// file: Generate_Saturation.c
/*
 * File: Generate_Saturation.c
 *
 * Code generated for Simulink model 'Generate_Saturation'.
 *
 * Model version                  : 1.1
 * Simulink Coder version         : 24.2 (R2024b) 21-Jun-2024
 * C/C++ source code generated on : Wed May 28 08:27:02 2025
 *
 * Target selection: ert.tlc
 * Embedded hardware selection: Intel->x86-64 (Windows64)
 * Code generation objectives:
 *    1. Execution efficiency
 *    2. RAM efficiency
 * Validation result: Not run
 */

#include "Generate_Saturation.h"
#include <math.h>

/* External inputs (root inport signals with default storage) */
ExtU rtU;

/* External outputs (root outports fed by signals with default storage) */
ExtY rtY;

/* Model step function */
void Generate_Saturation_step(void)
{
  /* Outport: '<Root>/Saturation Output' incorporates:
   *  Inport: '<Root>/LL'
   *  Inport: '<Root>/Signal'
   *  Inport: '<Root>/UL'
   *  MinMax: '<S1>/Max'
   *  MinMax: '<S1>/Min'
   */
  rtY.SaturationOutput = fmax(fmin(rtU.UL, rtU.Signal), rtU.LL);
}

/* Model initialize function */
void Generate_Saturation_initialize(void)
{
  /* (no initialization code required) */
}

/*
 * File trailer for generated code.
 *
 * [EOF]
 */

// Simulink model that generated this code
simulink model "Generate_Saturation"  (R2024b)
settings: Solver=FixedStepDiscrete  StartTime=0.0  StopTime=10.0  FixedStep=0.001  RelTol=1e-3

== system Generate_Saturation ==
  Signal : Inport
  UL : Inport  Port=2
  LL : Inport  Port=3
  Saturation : Subsystem
  Saturation Output : Outport
  wires:
  Signal/1 -> Saturation/2(Signal)
  UL/1 -> Saturation/1(UL)
  LL/1 -> Saturation/3(LL)
  Saturation/1(Out1) -> Saturation Output/1

== system Generate_Saturation/Saturation ==
  UL : Inport
  Signal : Inport  Port=2
  LL : Inport  Port=3
  Max : MinMax  Function=max  Inputs=2
  Min : MinMax  Inputs=2
  Out1 : Outport
  wires:
  Min/1 -> Max/1
  Signal/1 -> Min/2
  UL/1 -> Min/1
  Max/1 -> Out1/1
  LL/1 -> Max/2
